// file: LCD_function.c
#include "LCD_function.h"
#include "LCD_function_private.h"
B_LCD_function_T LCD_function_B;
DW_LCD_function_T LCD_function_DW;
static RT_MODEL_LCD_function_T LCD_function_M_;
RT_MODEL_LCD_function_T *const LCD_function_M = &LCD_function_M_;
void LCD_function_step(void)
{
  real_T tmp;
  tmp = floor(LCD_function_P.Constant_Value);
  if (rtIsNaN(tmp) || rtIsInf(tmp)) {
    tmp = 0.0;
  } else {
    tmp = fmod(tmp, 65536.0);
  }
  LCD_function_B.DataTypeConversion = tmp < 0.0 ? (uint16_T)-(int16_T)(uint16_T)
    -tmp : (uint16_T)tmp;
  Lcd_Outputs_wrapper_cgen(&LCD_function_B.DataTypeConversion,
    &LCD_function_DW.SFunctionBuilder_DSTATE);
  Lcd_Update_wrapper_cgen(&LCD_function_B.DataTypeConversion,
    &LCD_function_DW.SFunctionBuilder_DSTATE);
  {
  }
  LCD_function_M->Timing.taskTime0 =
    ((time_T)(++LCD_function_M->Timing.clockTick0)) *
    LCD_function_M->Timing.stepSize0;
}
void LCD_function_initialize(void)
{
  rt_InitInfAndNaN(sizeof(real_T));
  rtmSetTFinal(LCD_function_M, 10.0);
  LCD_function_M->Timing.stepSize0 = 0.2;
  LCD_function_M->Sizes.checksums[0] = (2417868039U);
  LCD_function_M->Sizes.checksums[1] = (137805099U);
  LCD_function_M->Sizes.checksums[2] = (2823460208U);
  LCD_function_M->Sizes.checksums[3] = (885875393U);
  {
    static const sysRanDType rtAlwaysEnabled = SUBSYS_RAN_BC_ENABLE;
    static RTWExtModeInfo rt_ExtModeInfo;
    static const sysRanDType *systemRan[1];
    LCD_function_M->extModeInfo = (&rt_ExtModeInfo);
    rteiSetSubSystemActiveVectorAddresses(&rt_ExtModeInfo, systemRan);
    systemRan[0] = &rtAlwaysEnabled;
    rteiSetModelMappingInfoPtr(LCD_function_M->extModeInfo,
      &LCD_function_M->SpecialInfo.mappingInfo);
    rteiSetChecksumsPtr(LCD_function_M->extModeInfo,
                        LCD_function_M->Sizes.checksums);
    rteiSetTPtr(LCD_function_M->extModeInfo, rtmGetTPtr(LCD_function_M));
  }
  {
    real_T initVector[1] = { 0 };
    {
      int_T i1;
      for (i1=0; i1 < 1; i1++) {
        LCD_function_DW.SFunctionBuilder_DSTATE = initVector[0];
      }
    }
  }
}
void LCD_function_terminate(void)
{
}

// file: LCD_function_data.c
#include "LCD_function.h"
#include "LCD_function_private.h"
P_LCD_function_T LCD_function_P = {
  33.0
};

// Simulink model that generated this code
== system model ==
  SFunctionBuilder : S-Function  FunctionName=Lcd  <- 1: DataTypeConversion
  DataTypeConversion : DataTypeConversion  <- 1: Constant
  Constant : Constant  Value=33
